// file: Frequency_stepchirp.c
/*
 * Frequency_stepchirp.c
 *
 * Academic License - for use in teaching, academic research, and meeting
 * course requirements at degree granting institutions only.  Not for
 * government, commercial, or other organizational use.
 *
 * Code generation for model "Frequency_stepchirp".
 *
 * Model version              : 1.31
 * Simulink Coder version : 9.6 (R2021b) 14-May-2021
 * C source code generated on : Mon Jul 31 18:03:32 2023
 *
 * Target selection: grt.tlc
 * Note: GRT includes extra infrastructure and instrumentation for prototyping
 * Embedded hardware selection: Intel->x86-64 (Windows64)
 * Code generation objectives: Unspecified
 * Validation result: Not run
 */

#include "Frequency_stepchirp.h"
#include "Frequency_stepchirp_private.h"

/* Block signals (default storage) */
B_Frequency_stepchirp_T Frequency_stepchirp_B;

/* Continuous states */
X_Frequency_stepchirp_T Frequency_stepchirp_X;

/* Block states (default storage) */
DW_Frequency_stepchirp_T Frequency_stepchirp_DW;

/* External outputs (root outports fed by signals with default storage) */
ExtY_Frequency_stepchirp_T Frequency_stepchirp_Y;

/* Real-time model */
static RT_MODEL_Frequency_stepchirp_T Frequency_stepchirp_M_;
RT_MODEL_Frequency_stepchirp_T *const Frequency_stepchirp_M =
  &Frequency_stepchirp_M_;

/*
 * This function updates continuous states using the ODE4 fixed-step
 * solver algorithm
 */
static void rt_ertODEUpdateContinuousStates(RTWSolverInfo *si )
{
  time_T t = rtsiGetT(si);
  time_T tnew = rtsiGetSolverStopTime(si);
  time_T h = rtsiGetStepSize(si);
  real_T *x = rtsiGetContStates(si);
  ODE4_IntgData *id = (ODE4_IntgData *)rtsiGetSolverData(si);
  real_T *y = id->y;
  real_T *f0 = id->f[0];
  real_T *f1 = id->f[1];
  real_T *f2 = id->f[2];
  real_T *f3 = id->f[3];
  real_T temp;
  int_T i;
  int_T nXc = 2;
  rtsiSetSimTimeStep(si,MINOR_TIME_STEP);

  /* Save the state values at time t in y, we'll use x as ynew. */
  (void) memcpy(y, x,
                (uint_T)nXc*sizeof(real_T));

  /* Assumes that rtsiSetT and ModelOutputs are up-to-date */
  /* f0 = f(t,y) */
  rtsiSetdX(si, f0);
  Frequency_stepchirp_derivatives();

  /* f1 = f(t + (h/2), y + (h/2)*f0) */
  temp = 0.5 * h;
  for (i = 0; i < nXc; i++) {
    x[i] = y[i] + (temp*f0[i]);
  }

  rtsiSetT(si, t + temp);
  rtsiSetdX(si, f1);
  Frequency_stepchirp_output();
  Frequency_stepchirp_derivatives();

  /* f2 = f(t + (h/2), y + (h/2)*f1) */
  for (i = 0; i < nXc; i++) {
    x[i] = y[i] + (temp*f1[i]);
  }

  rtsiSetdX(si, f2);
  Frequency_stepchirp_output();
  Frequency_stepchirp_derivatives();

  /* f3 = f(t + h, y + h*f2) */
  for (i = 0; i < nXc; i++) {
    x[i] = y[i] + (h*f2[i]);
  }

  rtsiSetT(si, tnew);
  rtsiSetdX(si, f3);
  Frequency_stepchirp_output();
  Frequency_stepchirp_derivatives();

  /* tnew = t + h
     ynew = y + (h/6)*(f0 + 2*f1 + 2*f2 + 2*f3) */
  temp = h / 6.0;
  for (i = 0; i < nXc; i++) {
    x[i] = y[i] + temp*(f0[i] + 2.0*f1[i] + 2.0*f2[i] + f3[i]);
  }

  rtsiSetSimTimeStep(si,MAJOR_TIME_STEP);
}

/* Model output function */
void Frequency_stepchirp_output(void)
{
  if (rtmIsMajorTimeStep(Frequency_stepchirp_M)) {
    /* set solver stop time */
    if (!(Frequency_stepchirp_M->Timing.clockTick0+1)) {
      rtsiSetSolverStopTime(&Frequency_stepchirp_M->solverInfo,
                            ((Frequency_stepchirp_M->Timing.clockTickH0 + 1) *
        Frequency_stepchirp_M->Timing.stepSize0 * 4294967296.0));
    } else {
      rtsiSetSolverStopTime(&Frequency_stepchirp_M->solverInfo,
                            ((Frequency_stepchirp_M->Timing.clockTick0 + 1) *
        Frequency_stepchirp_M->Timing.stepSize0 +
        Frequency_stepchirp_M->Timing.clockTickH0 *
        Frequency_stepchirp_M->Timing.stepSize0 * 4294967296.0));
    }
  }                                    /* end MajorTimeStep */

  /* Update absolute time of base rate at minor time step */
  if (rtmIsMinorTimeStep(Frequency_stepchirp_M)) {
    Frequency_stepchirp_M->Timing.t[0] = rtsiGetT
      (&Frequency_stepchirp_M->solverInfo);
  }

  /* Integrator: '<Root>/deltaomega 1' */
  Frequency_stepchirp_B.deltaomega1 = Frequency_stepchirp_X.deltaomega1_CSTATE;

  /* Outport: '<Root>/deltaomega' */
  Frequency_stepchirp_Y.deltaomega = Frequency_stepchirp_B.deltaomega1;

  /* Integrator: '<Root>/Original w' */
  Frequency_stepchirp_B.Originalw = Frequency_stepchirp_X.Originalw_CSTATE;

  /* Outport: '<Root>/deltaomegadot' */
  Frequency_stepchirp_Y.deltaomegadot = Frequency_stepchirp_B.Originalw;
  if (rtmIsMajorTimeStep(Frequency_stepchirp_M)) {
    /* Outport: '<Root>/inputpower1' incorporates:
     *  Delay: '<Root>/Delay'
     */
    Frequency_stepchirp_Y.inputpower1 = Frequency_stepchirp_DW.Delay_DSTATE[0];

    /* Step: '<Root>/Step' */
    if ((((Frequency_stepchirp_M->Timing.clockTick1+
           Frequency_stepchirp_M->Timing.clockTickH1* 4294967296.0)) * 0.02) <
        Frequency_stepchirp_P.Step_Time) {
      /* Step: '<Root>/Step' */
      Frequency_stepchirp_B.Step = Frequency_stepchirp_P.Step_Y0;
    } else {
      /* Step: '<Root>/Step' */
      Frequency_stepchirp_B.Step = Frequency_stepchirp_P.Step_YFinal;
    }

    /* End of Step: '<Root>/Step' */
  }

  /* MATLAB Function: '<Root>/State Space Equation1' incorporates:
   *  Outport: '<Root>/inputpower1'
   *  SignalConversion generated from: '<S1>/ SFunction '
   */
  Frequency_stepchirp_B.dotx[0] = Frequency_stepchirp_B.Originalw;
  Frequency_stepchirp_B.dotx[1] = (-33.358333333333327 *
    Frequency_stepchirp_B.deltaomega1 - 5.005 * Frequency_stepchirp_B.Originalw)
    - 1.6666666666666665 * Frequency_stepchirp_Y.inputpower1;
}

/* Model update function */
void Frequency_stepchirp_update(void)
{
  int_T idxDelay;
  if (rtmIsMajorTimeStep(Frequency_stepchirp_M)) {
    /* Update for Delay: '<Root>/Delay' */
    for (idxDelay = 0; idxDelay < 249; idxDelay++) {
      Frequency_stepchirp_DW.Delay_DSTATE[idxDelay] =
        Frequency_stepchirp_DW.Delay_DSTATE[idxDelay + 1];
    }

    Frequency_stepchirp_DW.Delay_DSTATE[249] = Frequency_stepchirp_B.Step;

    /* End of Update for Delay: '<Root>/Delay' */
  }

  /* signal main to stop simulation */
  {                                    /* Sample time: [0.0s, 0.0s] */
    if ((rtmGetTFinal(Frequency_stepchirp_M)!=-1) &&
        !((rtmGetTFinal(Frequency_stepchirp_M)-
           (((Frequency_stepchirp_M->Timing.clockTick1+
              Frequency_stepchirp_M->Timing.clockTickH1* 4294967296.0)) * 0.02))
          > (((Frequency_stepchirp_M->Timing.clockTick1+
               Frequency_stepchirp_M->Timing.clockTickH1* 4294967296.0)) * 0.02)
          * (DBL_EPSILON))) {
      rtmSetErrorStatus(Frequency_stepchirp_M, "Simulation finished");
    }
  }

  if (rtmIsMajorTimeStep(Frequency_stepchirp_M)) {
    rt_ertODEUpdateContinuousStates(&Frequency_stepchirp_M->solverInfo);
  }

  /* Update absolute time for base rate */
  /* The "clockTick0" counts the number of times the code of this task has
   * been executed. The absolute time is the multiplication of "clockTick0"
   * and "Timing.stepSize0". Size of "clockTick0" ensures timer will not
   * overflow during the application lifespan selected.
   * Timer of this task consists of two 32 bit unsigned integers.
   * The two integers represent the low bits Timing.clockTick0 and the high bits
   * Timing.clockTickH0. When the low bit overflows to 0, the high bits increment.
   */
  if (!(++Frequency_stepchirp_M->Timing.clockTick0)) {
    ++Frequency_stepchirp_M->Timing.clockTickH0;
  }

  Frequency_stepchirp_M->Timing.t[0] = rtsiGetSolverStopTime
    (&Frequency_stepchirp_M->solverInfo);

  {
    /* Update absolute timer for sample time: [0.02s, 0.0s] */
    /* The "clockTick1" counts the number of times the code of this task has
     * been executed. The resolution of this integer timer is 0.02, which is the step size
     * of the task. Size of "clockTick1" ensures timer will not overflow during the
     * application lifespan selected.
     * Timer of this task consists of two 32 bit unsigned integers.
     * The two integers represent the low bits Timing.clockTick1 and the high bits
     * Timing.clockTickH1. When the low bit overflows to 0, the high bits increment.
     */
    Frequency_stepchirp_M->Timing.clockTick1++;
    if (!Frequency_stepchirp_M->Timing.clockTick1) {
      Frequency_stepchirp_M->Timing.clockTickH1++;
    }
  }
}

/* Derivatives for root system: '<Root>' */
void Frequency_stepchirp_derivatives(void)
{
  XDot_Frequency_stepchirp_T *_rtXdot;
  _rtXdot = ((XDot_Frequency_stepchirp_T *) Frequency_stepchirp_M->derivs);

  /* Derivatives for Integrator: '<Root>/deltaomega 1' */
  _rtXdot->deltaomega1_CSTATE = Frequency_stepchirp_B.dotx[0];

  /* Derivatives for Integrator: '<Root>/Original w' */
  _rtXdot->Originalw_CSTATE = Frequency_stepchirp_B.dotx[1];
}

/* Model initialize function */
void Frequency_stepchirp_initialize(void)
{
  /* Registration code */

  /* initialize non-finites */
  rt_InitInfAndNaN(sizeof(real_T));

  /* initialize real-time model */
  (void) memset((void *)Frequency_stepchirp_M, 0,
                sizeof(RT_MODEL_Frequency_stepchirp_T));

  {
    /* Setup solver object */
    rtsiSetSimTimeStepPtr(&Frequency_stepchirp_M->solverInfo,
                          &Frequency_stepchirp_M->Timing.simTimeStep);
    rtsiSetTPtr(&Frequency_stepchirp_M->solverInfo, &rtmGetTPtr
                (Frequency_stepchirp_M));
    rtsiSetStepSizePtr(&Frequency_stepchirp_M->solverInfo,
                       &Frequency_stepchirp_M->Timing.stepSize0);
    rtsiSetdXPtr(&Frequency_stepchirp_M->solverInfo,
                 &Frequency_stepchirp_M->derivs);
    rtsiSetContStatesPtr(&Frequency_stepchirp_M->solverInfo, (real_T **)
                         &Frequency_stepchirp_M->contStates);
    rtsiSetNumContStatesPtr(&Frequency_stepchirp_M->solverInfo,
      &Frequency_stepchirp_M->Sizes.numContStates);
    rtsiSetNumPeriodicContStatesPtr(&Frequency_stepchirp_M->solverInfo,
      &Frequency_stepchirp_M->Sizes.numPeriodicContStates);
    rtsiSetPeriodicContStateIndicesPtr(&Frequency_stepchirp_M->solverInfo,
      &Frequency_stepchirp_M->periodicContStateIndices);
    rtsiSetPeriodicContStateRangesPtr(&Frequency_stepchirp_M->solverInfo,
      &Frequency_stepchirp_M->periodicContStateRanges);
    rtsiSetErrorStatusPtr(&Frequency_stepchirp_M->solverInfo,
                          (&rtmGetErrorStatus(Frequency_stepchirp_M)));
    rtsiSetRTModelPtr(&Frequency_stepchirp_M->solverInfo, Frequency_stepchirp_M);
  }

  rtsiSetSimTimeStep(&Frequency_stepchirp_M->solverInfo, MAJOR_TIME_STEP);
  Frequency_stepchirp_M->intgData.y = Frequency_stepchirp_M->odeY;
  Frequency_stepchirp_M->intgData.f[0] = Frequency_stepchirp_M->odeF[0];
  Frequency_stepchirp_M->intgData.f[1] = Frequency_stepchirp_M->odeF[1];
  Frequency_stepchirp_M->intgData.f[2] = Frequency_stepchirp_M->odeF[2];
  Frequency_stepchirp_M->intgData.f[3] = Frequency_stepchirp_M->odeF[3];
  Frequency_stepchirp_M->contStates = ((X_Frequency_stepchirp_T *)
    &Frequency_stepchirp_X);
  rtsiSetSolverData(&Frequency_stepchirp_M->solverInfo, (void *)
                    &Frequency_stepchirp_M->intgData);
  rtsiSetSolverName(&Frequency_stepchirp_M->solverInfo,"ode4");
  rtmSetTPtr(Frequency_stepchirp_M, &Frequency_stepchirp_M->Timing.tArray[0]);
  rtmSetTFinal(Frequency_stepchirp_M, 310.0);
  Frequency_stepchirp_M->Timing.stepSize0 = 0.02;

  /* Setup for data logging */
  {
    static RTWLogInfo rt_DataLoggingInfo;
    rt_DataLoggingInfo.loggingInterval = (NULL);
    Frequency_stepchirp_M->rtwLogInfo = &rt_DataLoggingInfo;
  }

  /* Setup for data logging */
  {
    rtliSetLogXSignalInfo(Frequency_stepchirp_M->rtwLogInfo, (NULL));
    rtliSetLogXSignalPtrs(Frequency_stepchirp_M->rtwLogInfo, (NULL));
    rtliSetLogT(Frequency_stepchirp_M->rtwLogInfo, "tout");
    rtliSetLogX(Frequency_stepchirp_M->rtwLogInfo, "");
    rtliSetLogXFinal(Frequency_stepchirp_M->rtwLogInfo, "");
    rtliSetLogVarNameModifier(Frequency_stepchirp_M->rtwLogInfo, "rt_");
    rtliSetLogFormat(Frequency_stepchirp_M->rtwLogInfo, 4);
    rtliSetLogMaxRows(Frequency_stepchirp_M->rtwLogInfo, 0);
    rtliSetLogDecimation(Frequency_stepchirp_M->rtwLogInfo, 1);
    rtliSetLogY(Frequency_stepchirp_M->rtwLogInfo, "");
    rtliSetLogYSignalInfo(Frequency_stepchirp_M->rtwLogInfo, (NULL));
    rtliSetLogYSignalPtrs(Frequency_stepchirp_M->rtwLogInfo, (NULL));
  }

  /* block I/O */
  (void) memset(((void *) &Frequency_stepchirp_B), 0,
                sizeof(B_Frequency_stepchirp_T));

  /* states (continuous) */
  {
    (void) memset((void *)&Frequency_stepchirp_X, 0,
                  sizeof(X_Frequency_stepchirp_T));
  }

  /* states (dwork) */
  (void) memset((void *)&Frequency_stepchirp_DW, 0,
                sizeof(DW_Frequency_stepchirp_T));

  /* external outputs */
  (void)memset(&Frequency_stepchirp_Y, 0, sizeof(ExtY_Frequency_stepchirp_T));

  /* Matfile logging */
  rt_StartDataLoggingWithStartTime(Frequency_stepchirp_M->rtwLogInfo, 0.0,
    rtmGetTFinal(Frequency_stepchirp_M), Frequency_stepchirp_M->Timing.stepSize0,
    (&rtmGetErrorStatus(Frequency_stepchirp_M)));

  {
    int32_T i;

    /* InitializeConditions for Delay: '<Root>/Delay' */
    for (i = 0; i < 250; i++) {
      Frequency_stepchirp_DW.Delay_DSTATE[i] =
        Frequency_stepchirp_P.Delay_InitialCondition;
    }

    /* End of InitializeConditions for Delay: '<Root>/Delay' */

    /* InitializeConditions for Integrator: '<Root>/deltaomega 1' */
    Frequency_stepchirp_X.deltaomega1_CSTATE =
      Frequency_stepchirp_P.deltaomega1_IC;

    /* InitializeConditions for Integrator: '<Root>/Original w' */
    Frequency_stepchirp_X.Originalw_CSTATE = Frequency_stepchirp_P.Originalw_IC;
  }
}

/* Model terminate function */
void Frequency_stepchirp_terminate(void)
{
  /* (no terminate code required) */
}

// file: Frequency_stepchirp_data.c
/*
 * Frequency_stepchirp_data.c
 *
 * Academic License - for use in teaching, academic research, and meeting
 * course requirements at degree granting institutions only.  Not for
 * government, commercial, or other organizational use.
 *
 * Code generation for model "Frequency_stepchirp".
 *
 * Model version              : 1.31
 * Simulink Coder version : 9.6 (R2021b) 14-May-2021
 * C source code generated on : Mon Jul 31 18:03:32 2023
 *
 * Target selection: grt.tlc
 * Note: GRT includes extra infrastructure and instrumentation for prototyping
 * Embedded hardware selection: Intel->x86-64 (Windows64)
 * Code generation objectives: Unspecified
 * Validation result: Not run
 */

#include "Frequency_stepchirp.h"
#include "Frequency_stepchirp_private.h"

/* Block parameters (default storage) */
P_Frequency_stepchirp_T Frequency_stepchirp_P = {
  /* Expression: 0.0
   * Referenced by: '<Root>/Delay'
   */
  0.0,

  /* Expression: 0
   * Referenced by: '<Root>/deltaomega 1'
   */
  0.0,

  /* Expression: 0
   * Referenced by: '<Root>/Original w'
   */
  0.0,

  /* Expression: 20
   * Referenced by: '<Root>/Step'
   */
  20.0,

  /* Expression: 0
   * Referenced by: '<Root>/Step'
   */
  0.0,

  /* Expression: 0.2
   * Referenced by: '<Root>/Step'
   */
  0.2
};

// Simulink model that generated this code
simulink model "Frequency_stepchirp"  (R2021b)
settings: Solver=ode4  StartTime=0.0  StopTime=310  FixedStep=0.02  RelTol=1e-3

== system Frequency_stepchirp ==
  Delay : Delay  DelayLength=250
  Demux1 : Demux  Outputs=2
  Mux1 : Mux  Inputs=2
  Original w : Integrator
  Pulse Generator1 : DiscretePulseGenerator  Commented=on  PulseType=Time based  Amplitude=0.1  Period=1  PulseWidth=50
  Scope6 : Scope
  Scope7 : Scope  NumInputPorts=2
  State Space Equation1 : MATLAB Function  TreatAsAtomicUnit=on
  Step : Step  Time=20  After=0.2  SampleTime=0.02
  deltaomega 1 : Integrator
  inputpower1 : Outport
  deltaomega : Outport  Port=2
  deltaomegadot : Outport  Port=3
  wires:
  Demux1/1 -> deltaomega 1/1
  Delay/1 -> inputpower1/1, Scope6/1, State Space Equation1/2(u)
  Mux1/1 -> State Space Equation1/1(x)
  deltaomega 1/1 -> deltaomega/1, Scope7/1, Mux1/1
  Demux1/2 -> Original w/1
  Original w/1 -> Mux1/2, Scope7/2, deltaomegadot/1
  State Space Equation1/1(dotx) -> Demux1/1
  Step/1 -> Delay/1

== matlab function Frequency_stepchirp/State Space Equation1 ==
function dotx  = fcn(x, u)
D = 1.5/100;
M = 3.0;
    Tg = 0.2;
    Rp = 0.05;
    Ki=2;
    dotx = zeros(2, 1);
    %x1 = x(1);
    x1 = x(1);
    x2=x(2);
    dotx = [x2;-(D/(M*Tg)+1/(Rp*M*Tg))*x1-(D/M+1/Tg)*x2-1/(M*Tg)*u];
